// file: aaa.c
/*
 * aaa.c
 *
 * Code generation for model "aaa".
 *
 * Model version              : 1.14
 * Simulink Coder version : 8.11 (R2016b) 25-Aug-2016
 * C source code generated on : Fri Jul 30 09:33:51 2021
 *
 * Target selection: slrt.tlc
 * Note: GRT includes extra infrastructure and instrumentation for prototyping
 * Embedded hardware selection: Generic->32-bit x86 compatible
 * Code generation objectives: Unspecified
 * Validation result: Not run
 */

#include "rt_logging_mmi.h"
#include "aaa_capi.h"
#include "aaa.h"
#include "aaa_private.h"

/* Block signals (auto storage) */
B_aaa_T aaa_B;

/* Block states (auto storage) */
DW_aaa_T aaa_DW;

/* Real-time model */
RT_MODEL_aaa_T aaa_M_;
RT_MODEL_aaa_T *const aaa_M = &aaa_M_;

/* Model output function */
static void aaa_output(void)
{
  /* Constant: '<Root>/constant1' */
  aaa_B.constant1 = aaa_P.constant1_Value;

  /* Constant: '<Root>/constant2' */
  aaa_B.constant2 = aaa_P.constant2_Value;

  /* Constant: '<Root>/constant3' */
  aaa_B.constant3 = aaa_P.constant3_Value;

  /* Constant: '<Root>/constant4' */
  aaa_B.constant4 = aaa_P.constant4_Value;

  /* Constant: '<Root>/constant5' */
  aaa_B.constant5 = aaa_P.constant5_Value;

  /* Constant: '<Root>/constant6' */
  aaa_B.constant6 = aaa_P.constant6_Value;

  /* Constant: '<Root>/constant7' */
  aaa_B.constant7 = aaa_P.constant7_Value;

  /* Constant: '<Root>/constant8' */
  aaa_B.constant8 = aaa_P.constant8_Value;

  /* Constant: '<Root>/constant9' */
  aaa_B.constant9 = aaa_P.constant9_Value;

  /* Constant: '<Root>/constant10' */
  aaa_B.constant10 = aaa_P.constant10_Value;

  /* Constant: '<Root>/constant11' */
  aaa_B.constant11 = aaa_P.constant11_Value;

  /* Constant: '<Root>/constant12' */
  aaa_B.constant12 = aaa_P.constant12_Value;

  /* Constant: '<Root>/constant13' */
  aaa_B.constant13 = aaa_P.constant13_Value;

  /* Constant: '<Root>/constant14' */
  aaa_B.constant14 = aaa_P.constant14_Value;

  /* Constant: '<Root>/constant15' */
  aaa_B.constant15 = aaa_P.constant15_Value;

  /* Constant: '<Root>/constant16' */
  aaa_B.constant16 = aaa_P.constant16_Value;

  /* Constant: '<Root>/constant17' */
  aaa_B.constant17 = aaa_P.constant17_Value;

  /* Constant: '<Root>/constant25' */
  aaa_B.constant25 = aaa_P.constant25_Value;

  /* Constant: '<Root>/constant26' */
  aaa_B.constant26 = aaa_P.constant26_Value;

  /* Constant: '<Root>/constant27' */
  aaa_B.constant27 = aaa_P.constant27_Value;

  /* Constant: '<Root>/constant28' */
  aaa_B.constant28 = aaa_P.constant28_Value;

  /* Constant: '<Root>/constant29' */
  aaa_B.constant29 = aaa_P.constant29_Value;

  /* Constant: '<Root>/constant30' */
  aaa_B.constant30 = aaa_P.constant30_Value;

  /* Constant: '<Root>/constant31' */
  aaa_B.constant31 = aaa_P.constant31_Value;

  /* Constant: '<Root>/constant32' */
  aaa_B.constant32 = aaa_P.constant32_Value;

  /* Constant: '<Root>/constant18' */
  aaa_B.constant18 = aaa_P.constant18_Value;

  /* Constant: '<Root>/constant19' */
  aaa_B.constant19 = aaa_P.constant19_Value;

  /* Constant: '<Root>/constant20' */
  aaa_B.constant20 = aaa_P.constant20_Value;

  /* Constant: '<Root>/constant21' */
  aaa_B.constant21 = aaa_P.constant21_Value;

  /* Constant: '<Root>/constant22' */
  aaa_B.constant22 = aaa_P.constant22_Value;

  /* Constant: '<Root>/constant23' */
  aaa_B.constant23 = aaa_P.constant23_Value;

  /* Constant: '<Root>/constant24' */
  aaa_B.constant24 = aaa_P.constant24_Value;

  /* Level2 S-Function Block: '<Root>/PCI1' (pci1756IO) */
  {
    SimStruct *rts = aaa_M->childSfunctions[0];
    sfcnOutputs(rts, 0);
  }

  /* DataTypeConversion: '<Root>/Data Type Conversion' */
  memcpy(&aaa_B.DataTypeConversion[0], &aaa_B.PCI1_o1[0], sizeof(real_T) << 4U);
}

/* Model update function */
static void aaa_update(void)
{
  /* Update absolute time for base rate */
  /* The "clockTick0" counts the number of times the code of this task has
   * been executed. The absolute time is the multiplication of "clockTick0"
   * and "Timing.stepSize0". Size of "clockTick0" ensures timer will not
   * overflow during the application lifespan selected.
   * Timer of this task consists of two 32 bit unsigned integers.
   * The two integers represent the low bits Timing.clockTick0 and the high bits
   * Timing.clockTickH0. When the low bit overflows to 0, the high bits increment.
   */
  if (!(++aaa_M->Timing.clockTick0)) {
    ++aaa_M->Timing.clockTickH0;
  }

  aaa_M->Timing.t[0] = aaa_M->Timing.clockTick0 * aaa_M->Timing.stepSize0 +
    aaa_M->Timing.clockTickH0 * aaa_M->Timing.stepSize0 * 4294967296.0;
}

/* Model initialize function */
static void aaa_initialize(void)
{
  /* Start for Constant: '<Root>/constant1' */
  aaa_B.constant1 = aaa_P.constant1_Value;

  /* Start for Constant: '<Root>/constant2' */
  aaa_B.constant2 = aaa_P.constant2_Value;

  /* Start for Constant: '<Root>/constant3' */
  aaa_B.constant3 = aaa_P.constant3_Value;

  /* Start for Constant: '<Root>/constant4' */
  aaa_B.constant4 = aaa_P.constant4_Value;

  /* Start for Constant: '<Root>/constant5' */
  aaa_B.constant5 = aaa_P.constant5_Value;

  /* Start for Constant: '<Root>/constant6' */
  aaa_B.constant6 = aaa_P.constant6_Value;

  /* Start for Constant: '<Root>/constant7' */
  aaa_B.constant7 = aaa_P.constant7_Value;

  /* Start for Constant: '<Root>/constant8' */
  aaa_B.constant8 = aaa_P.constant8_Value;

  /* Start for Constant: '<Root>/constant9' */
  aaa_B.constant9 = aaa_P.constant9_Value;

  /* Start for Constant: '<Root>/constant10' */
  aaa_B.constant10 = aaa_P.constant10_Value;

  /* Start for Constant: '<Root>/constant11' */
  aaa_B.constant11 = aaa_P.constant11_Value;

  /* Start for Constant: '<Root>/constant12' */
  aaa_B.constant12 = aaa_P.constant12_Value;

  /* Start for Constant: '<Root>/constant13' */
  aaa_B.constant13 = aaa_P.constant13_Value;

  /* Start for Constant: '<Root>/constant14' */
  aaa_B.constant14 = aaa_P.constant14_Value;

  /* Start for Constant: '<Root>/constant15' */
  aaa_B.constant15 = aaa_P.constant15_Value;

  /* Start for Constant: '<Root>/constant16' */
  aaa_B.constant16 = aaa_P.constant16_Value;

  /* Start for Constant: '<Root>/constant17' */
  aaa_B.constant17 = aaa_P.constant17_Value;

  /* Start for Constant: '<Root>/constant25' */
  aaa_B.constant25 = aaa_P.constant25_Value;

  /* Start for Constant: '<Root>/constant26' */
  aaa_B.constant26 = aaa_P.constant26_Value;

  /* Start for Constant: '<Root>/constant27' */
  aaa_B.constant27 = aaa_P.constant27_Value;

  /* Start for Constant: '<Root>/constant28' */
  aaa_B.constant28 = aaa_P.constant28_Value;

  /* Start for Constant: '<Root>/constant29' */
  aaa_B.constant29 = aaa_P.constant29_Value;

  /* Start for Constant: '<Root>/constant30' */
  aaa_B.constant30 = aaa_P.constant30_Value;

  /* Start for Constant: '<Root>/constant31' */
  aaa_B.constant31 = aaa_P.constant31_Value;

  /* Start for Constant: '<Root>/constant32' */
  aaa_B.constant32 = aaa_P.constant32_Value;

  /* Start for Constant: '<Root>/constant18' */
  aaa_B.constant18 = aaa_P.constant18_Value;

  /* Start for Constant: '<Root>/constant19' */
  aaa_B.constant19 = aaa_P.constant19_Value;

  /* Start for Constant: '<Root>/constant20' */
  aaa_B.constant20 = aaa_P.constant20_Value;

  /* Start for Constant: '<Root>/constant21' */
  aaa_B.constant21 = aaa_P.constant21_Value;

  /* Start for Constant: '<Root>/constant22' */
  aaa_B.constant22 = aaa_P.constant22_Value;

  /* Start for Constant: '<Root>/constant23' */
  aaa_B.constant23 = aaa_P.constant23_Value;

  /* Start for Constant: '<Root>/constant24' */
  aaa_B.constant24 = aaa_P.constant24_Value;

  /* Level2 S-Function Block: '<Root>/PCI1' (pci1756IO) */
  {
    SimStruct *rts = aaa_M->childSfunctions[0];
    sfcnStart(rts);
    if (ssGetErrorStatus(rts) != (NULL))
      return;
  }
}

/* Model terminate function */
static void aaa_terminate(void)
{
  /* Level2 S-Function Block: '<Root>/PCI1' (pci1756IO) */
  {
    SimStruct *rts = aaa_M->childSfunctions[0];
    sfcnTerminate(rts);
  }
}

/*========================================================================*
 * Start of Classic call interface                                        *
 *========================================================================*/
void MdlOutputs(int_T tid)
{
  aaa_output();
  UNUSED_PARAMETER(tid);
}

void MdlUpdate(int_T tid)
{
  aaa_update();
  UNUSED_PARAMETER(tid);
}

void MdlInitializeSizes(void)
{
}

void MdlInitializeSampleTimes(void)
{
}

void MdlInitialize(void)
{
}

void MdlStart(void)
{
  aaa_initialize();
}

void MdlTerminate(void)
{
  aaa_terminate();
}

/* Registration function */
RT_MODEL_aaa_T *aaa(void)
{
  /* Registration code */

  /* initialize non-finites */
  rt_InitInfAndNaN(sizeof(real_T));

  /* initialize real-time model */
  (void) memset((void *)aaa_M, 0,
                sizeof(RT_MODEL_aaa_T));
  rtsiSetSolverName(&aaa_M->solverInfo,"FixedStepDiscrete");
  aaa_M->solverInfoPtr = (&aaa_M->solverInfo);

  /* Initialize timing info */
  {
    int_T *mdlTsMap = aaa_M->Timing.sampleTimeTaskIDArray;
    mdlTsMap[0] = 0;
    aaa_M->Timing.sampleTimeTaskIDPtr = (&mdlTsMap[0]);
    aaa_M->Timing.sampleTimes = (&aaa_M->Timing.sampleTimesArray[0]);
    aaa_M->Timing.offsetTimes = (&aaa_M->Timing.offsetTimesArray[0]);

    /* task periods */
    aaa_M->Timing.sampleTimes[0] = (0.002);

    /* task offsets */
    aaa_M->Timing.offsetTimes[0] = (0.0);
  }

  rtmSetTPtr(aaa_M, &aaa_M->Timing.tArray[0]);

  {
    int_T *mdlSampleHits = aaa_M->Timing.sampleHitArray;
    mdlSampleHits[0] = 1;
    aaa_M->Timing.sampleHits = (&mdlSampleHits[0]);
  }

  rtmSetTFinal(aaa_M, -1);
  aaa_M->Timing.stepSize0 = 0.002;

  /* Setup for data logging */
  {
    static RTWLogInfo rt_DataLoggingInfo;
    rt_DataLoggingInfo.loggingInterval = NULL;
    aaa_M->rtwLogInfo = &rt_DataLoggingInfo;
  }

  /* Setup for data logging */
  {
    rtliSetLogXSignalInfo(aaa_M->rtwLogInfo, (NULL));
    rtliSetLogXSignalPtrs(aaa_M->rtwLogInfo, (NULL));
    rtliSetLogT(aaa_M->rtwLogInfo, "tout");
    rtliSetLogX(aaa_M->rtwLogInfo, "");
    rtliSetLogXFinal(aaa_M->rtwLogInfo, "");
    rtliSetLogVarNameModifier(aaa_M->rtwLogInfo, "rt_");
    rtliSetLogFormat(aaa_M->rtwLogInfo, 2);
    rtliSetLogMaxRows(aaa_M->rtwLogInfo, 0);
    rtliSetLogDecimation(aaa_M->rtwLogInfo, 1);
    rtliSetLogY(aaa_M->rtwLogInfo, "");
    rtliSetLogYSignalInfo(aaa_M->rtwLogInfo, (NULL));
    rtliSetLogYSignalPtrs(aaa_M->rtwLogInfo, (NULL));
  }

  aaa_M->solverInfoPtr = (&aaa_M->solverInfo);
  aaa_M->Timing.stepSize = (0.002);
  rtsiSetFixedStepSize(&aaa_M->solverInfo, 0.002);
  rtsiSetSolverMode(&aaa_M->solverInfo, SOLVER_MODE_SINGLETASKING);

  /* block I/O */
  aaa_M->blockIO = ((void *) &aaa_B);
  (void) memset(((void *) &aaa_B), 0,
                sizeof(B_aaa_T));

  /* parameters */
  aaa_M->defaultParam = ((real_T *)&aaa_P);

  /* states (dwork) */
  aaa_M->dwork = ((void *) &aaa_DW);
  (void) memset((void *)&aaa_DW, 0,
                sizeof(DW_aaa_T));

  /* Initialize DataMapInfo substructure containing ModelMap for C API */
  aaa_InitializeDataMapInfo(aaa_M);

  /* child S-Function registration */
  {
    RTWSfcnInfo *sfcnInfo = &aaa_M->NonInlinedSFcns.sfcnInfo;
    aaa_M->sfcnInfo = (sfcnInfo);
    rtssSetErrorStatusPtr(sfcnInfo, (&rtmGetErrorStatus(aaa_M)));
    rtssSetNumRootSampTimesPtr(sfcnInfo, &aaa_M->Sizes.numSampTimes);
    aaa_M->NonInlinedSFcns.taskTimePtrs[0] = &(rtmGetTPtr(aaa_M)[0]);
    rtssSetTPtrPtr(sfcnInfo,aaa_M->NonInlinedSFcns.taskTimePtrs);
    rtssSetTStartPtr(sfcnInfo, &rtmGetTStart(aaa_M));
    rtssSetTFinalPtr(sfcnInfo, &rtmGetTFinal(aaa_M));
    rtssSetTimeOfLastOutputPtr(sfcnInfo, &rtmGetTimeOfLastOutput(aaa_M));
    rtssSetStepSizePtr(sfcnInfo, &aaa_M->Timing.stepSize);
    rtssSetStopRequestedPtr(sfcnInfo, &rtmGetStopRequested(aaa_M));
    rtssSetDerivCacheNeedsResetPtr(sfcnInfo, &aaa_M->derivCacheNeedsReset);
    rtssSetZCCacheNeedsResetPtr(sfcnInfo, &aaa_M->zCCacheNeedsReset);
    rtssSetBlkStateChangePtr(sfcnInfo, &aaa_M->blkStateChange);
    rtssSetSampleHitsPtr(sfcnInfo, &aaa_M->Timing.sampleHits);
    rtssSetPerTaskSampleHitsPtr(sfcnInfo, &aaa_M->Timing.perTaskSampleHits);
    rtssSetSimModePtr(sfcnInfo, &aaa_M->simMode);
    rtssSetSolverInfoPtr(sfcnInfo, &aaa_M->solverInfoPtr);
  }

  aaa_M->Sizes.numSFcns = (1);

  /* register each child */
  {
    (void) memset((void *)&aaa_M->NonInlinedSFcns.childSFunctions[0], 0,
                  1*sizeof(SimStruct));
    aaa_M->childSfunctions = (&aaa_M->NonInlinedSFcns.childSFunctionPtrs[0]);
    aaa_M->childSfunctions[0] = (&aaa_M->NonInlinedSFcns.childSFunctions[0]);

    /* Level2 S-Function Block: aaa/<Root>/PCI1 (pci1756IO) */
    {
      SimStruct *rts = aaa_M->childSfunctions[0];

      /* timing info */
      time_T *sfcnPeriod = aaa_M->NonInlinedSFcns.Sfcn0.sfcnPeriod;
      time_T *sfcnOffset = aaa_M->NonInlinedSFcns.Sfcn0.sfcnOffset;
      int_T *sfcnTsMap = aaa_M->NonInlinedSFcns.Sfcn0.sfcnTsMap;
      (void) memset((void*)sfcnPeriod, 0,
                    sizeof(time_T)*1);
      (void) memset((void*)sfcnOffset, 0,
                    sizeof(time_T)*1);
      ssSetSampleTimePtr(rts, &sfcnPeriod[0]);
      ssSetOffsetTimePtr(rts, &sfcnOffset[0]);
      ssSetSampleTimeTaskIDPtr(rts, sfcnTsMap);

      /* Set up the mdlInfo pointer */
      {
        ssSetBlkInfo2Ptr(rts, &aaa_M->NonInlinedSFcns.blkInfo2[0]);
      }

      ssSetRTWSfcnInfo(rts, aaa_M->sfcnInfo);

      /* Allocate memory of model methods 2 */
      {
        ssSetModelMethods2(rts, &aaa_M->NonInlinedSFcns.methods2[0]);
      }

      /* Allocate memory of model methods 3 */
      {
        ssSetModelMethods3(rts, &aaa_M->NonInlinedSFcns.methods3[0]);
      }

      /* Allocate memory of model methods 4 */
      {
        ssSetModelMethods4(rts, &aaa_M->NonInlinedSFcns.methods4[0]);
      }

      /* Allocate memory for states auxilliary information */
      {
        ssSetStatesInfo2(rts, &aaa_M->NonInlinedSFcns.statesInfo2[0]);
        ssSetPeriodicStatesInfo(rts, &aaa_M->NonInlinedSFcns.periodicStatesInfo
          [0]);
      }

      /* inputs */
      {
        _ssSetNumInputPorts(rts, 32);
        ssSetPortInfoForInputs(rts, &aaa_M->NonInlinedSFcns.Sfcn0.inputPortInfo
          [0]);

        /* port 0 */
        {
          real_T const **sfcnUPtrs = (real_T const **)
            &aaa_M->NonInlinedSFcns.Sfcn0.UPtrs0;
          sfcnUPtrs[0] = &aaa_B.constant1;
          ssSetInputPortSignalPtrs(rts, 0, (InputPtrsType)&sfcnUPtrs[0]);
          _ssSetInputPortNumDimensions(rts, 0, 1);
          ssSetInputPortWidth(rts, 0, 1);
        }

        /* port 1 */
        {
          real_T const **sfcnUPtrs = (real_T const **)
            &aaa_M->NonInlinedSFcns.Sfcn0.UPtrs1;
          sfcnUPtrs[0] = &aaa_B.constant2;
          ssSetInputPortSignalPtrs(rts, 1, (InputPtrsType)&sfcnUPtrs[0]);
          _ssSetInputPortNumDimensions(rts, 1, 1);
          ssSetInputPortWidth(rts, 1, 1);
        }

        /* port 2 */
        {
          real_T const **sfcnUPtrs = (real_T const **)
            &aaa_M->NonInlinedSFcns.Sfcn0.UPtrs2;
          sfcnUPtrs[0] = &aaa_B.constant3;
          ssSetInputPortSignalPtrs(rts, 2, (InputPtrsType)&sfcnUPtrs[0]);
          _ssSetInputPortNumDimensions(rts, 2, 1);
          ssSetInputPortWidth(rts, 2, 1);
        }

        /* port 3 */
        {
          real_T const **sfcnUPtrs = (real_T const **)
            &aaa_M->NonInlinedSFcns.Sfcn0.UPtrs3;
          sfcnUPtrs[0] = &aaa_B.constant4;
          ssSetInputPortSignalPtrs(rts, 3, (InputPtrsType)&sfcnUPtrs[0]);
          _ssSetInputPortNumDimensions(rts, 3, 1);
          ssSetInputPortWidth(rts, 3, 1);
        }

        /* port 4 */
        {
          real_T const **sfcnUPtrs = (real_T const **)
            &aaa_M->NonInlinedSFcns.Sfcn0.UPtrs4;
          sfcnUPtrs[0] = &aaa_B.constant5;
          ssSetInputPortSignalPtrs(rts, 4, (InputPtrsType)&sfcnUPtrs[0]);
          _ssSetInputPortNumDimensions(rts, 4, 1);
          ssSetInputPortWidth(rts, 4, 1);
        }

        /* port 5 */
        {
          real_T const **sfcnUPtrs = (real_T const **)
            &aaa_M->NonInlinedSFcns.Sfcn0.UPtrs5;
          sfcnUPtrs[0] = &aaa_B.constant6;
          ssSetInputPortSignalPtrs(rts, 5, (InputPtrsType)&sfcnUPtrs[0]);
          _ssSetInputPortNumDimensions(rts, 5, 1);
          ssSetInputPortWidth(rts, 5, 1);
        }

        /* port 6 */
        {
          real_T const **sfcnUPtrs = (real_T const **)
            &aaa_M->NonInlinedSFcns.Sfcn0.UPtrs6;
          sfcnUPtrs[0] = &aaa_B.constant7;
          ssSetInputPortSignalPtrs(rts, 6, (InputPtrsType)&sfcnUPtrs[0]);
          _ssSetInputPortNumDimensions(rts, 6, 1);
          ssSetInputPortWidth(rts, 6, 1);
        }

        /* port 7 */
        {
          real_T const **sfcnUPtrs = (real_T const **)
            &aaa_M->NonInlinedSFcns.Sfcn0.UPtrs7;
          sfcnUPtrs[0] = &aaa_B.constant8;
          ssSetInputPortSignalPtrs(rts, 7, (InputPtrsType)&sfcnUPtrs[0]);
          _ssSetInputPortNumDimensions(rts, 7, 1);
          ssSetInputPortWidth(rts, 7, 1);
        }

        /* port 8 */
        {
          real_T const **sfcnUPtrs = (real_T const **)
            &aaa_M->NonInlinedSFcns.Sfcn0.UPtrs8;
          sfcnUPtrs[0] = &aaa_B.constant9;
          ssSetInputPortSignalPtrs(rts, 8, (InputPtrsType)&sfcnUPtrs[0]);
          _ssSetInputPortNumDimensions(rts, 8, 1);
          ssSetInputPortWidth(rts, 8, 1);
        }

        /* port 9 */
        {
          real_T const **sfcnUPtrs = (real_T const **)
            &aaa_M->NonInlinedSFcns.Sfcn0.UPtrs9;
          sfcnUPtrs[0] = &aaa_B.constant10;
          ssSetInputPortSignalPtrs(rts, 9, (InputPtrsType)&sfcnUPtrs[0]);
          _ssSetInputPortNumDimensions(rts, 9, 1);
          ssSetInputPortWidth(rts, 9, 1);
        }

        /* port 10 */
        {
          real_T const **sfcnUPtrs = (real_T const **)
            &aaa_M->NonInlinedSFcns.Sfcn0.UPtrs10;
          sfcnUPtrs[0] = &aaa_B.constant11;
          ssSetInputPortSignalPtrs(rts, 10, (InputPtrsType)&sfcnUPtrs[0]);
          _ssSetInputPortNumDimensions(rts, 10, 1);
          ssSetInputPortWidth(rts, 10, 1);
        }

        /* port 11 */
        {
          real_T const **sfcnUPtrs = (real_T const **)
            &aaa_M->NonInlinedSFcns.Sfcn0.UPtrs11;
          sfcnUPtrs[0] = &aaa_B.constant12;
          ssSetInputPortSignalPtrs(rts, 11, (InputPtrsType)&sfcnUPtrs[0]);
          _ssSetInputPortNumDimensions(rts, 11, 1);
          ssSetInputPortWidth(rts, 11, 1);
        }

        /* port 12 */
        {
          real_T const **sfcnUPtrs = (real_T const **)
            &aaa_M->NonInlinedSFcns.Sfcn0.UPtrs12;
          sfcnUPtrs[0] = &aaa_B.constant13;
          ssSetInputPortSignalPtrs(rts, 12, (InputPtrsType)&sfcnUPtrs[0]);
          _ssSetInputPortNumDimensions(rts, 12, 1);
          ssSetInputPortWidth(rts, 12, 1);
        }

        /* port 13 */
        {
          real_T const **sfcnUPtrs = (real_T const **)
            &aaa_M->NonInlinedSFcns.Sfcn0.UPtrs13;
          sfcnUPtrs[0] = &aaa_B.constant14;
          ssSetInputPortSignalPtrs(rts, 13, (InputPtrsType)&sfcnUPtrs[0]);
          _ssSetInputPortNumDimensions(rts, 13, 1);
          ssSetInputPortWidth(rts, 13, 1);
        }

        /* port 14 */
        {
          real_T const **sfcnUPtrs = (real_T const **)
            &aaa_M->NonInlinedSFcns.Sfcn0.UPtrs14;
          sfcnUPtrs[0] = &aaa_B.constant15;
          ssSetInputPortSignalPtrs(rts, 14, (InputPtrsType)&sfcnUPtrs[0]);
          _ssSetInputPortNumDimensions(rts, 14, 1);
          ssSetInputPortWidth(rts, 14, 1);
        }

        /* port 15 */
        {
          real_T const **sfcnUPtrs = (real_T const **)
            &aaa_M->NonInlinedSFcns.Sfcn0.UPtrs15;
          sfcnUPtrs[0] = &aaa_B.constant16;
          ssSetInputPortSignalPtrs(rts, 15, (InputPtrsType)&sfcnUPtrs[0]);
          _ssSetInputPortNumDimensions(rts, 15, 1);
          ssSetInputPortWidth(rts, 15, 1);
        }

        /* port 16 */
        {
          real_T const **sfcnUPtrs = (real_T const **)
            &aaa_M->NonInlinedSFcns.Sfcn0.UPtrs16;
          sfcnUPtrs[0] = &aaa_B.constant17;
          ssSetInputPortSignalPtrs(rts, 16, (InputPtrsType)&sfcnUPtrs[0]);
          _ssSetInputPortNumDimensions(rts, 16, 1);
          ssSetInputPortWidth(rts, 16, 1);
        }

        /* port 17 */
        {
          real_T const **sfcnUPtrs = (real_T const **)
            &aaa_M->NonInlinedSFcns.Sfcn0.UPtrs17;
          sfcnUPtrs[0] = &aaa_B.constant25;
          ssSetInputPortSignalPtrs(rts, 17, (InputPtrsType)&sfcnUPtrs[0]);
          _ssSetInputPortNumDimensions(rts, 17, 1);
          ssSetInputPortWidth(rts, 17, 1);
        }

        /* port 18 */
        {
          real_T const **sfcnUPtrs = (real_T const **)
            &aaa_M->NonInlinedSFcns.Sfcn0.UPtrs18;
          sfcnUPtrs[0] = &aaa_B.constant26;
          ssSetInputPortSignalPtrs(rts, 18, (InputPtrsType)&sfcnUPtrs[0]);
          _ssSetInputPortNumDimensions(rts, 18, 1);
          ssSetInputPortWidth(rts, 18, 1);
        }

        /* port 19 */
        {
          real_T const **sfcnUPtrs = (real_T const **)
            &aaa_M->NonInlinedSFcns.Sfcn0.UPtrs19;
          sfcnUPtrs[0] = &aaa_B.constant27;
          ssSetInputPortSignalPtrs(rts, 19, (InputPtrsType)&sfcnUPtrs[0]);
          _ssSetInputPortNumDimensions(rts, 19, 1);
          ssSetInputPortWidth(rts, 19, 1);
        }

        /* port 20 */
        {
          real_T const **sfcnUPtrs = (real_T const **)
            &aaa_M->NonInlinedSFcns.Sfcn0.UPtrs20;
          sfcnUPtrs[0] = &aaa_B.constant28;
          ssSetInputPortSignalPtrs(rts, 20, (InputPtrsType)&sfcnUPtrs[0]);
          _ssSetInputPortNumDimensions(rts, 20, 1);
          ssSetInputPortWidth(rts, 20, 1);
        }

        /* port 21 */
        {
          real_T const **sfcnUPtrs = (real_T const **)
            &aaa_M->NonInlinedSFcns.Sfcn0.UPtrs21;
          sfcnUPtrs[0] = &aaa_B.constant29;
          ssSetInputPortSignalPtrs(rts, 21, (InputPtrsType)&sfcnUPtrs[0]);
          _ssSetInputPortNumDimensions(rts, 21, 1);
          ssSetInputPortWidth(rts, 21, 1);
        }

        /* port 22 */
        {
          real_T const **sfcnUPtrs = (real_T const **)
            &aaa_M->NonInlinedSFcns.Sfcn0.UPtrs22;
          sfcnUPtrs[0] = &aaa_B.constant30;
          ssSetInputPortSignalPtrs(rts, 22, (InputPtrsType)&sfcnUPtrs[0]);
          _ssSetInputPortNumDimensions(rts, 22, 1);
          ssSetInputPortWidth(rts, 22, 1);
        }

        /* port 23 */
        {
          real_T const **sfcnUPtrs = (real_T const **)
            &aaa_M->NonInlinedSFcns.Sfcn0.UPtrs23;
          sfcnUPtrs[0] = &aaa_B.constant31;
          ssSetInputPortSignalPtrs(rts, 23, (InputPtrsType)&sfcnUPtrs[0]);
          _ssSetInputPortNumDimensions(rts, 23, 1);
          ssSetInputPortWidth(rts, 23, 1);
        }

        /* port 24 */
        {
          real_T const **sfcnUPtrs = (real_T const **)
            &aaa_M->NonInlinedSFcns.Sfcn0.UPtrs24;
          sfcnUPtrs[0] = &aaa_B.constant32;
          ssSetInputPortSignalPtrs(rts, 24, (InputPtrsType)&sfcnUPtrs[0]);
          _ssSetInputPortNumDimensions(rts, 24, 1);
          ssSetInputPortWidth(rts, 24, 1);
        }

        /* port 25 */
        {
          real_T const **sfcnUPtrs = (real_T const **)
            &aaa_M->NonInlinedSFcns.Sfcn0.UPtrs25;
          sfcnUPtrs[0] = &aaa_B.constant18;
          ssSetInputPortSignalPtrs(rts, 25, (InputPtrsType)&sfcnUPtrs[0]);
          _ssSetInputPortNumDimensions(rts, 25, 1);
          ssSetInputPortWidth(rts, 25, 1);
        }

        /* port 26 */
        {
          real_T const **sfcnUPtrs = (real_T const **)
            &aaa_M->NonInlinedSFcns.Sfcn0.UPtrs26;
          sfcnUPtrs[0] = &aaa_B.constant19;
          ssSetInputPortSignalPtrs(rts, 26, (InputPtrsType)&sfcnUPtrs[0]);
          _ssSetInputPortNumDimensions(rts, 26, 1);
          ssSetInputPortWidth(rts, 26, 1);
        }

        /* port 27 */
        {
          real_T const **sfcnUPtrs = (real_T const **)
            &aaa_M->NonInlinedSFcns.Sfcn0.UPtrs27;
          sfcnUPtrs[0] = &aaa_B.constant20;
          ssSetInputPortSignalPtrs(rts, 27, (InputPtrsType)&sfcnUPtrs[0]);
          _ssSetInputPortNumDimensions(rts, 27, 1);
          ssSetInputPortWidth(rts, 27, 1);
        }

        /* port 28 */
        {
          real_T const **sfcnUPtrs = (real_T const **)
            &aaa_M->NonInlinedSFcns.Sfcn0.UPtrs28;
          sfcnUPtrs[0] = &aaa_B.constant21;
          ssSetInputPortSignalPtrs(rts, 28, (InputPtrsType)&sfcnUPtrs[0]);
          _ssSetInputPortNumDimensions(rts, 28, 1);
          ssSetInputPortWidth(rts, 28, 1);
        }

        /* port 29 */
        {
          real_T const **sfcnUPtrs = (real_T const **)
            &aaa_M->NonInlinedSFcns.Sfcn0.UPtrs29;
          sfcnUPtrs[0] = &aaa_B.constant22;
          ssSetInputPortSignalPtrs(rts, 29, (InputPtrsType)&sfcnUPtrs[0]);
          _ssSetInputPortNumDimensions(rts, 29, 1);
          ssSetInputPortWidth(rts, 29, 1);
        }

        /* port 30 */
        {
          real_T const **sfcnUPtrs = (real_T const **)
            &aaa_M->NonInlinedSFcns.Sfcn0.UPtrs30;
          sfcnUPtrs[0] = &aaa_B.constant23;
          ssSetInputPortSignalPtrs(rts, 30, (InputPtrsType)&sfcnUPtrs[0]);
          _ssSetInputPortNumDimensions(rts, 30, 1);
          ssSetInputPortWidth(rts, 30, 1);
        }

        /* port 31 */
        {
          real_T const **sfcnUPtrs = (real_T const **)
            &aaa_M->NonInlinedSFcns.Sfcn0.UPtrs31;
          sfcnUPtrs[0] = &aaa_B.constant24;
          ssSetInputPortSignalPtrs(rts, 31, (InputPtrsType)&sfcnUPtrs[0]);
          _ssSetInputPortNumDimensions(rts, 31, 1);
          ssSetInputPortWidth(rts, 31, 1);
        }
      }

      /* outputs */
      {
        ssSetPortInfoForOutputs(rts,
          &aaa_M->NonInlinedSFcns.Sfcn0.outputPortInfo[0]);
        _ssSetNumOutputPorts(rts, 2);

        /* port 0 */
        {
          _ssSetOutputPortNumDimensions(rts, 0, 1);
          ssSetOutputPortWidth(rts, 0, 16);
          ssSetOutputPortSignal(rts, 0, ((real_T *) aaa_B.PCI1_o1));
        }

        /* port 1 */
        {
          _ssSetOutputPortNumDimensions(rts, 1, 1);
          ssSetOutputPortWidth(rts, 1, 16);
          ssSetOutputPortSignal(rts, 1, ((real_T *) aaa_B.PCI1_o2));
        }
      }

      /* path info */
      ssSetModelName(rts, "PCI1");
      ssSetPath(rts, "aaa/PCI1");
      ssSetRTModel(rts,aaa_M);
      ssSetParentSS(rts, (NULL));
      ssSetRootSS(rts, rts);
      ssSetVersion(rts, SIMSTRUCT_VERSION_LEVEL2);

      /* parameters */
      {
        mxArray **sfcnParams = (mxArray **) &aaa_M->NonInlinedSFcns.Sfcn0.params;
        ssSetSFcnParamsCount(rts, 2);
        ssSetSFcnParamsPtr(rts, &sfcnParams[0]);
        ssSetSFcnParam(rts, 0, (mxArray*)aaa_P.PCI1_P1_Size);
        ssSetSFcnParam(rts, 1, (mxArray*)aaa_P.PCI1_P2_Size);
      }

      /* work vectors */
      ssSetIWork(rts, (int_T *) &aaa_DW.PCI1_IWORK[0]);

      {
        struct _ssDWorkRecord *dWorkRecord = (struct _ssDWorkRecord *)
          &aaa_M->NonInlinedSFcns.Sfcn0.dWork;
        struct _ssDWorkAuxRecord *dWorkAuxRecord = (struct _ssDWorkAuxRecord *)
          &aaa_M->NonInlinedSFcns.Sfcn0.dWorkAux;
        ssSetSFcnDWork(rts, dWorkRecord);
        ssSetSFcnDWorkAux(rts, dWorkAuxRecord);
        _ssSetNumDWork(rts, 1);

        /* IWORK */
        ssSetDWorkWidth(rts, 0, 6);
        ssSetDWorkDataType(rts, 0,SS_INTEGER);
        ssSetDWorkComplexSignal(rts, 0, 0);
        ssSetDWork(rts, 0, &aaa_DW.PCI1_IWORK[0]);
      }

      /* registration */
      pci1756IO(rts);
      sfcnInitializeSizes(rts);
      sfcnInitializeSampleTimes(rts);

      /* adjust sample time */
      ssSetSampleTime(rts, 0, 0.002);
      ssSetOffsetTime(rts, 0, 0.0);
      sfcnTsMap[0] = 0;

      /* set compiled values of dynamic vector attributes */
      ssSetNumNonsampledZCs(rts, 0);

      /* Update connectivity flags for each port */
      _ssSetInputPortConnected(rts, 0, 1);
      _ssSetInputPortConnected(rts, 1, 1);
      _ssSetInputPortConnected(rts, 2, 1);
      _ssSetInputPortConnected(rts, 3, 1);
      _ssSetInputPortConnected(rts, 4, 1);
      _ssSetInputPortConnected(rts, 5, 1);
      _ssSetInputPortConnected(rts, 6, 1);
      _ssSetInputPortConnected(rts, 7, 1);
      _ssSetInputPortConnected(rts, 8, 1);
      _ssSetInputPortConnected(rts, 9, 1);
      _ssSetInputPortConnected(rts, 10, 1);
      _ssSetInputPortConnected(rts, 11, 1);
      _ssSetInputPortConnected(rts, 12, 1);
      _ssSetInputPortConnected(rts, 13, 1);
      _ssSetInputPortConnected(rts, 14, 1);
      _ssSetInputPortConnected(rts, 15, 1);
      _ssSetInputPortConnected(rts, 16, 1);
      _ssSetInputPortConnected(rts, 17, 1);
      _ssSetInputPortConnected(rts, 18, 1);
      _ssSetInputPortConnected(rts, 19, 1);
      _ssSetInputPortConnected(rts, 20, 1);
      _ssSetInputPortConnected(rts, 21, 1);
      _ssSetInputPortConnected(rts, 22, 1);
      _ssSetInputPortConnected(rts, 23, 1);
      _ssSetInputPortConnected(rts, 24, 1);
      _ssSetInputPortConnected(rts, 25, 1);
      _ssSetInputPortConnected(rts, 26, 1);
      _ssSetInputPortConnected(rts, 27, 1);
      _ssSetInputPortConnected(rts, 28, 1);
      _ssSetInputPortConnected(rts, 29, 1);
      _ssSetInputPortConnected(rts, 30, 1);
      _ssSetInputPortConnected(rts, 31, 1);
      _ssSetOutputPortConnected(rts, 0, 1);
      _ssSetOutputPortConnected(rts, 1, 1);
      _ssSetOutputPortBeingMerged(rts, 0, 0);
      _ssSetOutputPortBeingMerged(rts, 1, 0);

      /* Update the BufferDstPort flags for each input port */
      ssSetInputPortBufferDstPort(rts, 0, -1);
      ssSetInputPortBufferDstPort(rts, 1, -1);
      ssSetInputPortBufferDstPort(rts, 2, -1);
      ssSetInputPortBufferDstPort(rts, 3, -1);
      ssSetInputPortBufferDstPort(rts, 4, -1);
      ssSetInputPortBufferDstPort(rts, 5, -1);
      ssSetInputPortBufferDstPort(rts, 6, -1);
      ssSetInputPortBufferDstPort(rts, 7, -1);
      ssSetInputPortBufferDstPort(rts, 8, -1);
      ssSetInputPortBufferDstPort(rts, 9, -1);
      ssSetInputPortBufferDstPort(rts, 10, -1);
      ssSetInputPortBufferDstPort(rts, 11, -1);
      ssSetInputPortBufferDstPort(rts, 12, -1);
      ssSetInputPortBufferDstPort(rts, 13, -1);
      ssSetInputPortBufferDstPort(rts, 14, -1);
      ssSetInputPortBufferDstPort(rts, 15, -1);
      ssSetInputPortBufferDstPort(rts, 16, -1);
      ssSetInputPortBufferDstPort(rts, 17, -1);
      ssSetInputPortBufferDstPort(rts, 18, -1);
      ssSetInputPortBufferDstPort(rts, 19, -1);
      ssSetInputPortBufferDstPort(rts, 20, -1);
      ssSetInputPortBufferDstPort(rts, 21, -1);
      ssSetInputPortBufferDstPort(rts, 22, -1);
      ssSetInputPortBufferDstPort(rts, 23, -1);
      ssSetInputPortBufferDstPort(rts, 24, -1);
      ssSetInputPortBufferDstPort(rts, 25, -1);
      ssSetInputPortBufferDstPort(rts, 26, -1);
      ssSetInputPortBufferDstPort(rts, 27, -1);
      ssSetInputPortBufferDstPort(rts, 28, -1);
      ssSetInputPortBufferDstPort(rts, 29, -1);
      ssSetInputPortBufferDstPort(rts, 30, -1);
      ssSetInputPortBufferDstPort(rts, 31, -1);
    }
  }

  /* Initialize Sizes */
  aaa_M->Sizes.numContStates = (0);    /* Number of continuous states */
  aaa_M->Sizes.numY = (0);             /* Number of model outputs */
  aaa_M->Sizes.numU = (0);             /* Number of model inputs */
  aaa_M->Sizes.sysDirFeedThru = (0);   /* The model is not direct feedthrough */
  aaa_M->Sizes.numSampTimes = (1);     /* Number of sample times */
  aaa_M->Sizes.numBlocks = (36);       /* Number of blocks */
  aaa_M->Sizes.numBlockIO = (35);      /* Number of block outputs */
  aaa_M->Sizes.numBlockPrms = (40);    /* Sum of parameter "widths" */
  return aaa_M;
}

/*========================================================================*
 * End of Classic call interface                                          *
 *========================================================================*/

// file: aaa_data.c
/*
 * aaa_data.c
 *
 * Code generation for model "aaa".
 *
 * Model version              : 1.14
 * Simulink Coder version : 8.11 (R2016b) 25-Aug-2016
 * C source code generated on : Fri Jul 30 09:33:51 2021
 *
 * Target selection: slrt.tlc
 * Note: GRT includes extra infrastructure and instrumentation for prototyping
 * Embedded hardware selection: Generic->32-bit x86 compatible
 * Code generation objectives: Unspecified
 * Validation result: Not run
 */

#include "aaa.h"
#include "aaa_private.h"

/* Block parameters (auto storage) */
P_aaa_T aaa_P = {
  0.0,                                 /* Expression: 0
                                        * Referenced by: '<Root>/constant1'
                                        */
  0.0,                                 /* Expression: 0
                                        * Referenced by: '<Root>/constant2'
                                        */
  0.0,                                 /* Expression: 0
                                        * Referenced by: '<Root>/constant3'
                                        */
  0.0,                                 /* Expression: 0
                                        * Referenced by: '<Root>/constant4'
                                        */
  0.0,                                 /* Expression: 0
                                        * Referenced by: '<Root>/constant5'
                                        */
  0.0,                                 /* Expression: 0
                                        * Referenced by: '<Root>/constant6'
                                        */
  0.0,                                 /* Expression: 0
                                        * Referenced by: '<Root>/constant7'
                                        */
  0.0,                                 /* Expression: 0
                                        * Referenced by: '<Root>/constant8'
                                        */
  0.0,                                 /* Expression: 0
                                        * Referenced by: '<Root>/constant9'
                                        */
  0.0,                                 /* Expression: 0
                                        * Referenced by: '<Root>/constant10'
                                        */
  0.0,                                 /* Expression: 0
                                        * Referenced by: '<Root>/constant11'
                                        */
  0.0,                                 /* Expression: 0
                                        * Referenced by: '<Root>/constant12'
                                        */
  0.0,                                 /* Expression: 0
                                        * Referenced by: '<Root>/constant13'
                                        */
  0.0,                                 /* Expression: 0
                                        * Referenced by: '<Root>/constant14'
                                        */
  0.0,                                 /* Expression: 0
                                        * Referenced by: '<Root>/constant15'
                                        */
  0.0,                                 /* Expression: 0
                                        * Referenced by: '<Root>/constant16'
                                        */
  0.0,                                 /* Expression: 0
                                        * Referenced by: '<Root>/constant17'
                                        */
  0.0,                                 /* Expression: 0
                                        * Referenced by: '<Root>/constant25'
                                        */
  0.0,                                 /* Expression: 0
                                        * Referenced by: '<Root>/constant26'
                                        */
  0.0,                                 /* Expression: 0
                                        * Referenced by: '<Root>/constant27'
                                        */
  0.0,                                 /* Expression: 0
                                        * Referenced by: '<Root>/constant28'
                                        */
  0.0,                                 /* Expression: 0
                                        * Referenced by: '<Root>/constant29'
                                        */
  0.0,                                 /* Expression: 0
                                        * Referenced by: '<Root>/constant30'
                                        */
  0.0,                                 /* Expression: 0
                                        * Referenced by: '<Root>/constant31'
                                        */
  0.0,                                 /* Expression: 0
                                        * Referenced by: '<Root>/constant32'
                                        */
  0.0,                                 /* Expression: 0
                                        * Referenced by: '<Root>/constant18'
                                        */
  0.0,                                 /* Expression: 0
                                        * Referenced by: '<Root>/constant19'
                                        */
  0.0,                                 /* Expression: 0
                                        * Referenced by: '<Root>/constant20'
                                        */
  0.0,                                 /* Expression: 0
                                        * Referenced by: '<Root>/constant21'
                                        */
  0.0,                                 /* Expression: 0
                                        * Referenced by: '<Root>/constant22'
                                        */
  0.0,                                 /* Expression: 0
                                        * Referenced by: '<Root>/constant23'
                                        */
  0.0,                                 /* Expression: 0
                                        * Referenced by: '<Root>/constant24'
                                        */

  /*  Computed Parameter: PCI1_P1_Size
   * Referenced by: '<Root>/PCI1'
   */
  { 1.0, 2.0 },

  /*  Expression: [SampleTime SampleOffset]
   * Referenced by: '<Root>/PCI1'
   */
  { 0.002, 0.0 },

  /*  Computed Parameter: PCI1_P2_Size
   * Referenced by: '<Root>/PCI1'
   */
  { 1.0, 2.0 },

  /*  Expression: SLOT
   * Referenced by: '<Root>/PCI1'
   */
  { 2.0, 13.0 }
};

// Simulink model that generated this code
simulink model "aaa"  (R2016b)
settings: Solver=ode4  StartTime=0.0  StopTime=inf  FixedStep=0.002  RelTol=1e-3  EnableMultiTasking=on

== system aaa ==
  Data Type Conversion : DataTypeConversion  OutDataTypeStr=double
  Display : Display
  Display1 : Display
  PCI1 : S-Function  FunctionName=pci1756IO  Parameters=[SampleTime SampleOffset], SLOT  SFunctionDeploymentMode=off  EnableBusSupport=off  mask(PCI1756){Sample=0.002, SLOT=[2 13]}
      mask prompts: Sample "Sample time:"
      mask help:
      | PCI-1756
      | Advantech
      | Digital Input&Output
      mask init:
      | SampleTime =0.002; SampleOffset=0;
  constant{1..32} (32 alike) : Constant  Value=0
  wires:
  constant2/1 -> PCI1/2
  constant3/1 -> PCI1/3
  constant4/1 -> PCI1/4
  constant5/1 -> PCI1/5
  constant6/1 -> PCI1/6
  constant7/1 -> PCI1/7
  constant8/1 -> PCI1/8
  constant9/1 -> PCI1/9
  constant10/1 -> PCI1/10
  constant11/1 -> PCI1/11
  constant12/1 -> PCI1/12
  constant13/1 -> PCI1/13
  constant14/1 -> PCI1/14
  constant15/1 -> PCI1/15
  constant16/1 -> PCI1/16
  constant17/1 -> PCI1/17
  constant25/1 -> PCI1/18
  constant26/1 -> PCI1/19
  constant27/1 -> PCI1/20
  constant28/1 -> PCI1/21
  constant29/1 -> PCI1/22
  constant30/1 -> PCI1/23
  constant31/1 -> PCI1/24
  constant32/1 -> PCI1/25
  constant18/1 -> PCI1/26
  constant19/1 -> PCI1/27
  constant20/1 -> PCI1/28
  constant21/1 -> PCI1/29
  constant22/1 -> PCI1/30
  constant23/1 -> PCI1/31
  constant24/1 -> PCI1/32
  constant1/1 -> PCI1/1
  PCI1/2 -> Display1/1
  Data Type Conversion/1 -> Display/1
  PCI1/1 -> Data Type Conversion/1
